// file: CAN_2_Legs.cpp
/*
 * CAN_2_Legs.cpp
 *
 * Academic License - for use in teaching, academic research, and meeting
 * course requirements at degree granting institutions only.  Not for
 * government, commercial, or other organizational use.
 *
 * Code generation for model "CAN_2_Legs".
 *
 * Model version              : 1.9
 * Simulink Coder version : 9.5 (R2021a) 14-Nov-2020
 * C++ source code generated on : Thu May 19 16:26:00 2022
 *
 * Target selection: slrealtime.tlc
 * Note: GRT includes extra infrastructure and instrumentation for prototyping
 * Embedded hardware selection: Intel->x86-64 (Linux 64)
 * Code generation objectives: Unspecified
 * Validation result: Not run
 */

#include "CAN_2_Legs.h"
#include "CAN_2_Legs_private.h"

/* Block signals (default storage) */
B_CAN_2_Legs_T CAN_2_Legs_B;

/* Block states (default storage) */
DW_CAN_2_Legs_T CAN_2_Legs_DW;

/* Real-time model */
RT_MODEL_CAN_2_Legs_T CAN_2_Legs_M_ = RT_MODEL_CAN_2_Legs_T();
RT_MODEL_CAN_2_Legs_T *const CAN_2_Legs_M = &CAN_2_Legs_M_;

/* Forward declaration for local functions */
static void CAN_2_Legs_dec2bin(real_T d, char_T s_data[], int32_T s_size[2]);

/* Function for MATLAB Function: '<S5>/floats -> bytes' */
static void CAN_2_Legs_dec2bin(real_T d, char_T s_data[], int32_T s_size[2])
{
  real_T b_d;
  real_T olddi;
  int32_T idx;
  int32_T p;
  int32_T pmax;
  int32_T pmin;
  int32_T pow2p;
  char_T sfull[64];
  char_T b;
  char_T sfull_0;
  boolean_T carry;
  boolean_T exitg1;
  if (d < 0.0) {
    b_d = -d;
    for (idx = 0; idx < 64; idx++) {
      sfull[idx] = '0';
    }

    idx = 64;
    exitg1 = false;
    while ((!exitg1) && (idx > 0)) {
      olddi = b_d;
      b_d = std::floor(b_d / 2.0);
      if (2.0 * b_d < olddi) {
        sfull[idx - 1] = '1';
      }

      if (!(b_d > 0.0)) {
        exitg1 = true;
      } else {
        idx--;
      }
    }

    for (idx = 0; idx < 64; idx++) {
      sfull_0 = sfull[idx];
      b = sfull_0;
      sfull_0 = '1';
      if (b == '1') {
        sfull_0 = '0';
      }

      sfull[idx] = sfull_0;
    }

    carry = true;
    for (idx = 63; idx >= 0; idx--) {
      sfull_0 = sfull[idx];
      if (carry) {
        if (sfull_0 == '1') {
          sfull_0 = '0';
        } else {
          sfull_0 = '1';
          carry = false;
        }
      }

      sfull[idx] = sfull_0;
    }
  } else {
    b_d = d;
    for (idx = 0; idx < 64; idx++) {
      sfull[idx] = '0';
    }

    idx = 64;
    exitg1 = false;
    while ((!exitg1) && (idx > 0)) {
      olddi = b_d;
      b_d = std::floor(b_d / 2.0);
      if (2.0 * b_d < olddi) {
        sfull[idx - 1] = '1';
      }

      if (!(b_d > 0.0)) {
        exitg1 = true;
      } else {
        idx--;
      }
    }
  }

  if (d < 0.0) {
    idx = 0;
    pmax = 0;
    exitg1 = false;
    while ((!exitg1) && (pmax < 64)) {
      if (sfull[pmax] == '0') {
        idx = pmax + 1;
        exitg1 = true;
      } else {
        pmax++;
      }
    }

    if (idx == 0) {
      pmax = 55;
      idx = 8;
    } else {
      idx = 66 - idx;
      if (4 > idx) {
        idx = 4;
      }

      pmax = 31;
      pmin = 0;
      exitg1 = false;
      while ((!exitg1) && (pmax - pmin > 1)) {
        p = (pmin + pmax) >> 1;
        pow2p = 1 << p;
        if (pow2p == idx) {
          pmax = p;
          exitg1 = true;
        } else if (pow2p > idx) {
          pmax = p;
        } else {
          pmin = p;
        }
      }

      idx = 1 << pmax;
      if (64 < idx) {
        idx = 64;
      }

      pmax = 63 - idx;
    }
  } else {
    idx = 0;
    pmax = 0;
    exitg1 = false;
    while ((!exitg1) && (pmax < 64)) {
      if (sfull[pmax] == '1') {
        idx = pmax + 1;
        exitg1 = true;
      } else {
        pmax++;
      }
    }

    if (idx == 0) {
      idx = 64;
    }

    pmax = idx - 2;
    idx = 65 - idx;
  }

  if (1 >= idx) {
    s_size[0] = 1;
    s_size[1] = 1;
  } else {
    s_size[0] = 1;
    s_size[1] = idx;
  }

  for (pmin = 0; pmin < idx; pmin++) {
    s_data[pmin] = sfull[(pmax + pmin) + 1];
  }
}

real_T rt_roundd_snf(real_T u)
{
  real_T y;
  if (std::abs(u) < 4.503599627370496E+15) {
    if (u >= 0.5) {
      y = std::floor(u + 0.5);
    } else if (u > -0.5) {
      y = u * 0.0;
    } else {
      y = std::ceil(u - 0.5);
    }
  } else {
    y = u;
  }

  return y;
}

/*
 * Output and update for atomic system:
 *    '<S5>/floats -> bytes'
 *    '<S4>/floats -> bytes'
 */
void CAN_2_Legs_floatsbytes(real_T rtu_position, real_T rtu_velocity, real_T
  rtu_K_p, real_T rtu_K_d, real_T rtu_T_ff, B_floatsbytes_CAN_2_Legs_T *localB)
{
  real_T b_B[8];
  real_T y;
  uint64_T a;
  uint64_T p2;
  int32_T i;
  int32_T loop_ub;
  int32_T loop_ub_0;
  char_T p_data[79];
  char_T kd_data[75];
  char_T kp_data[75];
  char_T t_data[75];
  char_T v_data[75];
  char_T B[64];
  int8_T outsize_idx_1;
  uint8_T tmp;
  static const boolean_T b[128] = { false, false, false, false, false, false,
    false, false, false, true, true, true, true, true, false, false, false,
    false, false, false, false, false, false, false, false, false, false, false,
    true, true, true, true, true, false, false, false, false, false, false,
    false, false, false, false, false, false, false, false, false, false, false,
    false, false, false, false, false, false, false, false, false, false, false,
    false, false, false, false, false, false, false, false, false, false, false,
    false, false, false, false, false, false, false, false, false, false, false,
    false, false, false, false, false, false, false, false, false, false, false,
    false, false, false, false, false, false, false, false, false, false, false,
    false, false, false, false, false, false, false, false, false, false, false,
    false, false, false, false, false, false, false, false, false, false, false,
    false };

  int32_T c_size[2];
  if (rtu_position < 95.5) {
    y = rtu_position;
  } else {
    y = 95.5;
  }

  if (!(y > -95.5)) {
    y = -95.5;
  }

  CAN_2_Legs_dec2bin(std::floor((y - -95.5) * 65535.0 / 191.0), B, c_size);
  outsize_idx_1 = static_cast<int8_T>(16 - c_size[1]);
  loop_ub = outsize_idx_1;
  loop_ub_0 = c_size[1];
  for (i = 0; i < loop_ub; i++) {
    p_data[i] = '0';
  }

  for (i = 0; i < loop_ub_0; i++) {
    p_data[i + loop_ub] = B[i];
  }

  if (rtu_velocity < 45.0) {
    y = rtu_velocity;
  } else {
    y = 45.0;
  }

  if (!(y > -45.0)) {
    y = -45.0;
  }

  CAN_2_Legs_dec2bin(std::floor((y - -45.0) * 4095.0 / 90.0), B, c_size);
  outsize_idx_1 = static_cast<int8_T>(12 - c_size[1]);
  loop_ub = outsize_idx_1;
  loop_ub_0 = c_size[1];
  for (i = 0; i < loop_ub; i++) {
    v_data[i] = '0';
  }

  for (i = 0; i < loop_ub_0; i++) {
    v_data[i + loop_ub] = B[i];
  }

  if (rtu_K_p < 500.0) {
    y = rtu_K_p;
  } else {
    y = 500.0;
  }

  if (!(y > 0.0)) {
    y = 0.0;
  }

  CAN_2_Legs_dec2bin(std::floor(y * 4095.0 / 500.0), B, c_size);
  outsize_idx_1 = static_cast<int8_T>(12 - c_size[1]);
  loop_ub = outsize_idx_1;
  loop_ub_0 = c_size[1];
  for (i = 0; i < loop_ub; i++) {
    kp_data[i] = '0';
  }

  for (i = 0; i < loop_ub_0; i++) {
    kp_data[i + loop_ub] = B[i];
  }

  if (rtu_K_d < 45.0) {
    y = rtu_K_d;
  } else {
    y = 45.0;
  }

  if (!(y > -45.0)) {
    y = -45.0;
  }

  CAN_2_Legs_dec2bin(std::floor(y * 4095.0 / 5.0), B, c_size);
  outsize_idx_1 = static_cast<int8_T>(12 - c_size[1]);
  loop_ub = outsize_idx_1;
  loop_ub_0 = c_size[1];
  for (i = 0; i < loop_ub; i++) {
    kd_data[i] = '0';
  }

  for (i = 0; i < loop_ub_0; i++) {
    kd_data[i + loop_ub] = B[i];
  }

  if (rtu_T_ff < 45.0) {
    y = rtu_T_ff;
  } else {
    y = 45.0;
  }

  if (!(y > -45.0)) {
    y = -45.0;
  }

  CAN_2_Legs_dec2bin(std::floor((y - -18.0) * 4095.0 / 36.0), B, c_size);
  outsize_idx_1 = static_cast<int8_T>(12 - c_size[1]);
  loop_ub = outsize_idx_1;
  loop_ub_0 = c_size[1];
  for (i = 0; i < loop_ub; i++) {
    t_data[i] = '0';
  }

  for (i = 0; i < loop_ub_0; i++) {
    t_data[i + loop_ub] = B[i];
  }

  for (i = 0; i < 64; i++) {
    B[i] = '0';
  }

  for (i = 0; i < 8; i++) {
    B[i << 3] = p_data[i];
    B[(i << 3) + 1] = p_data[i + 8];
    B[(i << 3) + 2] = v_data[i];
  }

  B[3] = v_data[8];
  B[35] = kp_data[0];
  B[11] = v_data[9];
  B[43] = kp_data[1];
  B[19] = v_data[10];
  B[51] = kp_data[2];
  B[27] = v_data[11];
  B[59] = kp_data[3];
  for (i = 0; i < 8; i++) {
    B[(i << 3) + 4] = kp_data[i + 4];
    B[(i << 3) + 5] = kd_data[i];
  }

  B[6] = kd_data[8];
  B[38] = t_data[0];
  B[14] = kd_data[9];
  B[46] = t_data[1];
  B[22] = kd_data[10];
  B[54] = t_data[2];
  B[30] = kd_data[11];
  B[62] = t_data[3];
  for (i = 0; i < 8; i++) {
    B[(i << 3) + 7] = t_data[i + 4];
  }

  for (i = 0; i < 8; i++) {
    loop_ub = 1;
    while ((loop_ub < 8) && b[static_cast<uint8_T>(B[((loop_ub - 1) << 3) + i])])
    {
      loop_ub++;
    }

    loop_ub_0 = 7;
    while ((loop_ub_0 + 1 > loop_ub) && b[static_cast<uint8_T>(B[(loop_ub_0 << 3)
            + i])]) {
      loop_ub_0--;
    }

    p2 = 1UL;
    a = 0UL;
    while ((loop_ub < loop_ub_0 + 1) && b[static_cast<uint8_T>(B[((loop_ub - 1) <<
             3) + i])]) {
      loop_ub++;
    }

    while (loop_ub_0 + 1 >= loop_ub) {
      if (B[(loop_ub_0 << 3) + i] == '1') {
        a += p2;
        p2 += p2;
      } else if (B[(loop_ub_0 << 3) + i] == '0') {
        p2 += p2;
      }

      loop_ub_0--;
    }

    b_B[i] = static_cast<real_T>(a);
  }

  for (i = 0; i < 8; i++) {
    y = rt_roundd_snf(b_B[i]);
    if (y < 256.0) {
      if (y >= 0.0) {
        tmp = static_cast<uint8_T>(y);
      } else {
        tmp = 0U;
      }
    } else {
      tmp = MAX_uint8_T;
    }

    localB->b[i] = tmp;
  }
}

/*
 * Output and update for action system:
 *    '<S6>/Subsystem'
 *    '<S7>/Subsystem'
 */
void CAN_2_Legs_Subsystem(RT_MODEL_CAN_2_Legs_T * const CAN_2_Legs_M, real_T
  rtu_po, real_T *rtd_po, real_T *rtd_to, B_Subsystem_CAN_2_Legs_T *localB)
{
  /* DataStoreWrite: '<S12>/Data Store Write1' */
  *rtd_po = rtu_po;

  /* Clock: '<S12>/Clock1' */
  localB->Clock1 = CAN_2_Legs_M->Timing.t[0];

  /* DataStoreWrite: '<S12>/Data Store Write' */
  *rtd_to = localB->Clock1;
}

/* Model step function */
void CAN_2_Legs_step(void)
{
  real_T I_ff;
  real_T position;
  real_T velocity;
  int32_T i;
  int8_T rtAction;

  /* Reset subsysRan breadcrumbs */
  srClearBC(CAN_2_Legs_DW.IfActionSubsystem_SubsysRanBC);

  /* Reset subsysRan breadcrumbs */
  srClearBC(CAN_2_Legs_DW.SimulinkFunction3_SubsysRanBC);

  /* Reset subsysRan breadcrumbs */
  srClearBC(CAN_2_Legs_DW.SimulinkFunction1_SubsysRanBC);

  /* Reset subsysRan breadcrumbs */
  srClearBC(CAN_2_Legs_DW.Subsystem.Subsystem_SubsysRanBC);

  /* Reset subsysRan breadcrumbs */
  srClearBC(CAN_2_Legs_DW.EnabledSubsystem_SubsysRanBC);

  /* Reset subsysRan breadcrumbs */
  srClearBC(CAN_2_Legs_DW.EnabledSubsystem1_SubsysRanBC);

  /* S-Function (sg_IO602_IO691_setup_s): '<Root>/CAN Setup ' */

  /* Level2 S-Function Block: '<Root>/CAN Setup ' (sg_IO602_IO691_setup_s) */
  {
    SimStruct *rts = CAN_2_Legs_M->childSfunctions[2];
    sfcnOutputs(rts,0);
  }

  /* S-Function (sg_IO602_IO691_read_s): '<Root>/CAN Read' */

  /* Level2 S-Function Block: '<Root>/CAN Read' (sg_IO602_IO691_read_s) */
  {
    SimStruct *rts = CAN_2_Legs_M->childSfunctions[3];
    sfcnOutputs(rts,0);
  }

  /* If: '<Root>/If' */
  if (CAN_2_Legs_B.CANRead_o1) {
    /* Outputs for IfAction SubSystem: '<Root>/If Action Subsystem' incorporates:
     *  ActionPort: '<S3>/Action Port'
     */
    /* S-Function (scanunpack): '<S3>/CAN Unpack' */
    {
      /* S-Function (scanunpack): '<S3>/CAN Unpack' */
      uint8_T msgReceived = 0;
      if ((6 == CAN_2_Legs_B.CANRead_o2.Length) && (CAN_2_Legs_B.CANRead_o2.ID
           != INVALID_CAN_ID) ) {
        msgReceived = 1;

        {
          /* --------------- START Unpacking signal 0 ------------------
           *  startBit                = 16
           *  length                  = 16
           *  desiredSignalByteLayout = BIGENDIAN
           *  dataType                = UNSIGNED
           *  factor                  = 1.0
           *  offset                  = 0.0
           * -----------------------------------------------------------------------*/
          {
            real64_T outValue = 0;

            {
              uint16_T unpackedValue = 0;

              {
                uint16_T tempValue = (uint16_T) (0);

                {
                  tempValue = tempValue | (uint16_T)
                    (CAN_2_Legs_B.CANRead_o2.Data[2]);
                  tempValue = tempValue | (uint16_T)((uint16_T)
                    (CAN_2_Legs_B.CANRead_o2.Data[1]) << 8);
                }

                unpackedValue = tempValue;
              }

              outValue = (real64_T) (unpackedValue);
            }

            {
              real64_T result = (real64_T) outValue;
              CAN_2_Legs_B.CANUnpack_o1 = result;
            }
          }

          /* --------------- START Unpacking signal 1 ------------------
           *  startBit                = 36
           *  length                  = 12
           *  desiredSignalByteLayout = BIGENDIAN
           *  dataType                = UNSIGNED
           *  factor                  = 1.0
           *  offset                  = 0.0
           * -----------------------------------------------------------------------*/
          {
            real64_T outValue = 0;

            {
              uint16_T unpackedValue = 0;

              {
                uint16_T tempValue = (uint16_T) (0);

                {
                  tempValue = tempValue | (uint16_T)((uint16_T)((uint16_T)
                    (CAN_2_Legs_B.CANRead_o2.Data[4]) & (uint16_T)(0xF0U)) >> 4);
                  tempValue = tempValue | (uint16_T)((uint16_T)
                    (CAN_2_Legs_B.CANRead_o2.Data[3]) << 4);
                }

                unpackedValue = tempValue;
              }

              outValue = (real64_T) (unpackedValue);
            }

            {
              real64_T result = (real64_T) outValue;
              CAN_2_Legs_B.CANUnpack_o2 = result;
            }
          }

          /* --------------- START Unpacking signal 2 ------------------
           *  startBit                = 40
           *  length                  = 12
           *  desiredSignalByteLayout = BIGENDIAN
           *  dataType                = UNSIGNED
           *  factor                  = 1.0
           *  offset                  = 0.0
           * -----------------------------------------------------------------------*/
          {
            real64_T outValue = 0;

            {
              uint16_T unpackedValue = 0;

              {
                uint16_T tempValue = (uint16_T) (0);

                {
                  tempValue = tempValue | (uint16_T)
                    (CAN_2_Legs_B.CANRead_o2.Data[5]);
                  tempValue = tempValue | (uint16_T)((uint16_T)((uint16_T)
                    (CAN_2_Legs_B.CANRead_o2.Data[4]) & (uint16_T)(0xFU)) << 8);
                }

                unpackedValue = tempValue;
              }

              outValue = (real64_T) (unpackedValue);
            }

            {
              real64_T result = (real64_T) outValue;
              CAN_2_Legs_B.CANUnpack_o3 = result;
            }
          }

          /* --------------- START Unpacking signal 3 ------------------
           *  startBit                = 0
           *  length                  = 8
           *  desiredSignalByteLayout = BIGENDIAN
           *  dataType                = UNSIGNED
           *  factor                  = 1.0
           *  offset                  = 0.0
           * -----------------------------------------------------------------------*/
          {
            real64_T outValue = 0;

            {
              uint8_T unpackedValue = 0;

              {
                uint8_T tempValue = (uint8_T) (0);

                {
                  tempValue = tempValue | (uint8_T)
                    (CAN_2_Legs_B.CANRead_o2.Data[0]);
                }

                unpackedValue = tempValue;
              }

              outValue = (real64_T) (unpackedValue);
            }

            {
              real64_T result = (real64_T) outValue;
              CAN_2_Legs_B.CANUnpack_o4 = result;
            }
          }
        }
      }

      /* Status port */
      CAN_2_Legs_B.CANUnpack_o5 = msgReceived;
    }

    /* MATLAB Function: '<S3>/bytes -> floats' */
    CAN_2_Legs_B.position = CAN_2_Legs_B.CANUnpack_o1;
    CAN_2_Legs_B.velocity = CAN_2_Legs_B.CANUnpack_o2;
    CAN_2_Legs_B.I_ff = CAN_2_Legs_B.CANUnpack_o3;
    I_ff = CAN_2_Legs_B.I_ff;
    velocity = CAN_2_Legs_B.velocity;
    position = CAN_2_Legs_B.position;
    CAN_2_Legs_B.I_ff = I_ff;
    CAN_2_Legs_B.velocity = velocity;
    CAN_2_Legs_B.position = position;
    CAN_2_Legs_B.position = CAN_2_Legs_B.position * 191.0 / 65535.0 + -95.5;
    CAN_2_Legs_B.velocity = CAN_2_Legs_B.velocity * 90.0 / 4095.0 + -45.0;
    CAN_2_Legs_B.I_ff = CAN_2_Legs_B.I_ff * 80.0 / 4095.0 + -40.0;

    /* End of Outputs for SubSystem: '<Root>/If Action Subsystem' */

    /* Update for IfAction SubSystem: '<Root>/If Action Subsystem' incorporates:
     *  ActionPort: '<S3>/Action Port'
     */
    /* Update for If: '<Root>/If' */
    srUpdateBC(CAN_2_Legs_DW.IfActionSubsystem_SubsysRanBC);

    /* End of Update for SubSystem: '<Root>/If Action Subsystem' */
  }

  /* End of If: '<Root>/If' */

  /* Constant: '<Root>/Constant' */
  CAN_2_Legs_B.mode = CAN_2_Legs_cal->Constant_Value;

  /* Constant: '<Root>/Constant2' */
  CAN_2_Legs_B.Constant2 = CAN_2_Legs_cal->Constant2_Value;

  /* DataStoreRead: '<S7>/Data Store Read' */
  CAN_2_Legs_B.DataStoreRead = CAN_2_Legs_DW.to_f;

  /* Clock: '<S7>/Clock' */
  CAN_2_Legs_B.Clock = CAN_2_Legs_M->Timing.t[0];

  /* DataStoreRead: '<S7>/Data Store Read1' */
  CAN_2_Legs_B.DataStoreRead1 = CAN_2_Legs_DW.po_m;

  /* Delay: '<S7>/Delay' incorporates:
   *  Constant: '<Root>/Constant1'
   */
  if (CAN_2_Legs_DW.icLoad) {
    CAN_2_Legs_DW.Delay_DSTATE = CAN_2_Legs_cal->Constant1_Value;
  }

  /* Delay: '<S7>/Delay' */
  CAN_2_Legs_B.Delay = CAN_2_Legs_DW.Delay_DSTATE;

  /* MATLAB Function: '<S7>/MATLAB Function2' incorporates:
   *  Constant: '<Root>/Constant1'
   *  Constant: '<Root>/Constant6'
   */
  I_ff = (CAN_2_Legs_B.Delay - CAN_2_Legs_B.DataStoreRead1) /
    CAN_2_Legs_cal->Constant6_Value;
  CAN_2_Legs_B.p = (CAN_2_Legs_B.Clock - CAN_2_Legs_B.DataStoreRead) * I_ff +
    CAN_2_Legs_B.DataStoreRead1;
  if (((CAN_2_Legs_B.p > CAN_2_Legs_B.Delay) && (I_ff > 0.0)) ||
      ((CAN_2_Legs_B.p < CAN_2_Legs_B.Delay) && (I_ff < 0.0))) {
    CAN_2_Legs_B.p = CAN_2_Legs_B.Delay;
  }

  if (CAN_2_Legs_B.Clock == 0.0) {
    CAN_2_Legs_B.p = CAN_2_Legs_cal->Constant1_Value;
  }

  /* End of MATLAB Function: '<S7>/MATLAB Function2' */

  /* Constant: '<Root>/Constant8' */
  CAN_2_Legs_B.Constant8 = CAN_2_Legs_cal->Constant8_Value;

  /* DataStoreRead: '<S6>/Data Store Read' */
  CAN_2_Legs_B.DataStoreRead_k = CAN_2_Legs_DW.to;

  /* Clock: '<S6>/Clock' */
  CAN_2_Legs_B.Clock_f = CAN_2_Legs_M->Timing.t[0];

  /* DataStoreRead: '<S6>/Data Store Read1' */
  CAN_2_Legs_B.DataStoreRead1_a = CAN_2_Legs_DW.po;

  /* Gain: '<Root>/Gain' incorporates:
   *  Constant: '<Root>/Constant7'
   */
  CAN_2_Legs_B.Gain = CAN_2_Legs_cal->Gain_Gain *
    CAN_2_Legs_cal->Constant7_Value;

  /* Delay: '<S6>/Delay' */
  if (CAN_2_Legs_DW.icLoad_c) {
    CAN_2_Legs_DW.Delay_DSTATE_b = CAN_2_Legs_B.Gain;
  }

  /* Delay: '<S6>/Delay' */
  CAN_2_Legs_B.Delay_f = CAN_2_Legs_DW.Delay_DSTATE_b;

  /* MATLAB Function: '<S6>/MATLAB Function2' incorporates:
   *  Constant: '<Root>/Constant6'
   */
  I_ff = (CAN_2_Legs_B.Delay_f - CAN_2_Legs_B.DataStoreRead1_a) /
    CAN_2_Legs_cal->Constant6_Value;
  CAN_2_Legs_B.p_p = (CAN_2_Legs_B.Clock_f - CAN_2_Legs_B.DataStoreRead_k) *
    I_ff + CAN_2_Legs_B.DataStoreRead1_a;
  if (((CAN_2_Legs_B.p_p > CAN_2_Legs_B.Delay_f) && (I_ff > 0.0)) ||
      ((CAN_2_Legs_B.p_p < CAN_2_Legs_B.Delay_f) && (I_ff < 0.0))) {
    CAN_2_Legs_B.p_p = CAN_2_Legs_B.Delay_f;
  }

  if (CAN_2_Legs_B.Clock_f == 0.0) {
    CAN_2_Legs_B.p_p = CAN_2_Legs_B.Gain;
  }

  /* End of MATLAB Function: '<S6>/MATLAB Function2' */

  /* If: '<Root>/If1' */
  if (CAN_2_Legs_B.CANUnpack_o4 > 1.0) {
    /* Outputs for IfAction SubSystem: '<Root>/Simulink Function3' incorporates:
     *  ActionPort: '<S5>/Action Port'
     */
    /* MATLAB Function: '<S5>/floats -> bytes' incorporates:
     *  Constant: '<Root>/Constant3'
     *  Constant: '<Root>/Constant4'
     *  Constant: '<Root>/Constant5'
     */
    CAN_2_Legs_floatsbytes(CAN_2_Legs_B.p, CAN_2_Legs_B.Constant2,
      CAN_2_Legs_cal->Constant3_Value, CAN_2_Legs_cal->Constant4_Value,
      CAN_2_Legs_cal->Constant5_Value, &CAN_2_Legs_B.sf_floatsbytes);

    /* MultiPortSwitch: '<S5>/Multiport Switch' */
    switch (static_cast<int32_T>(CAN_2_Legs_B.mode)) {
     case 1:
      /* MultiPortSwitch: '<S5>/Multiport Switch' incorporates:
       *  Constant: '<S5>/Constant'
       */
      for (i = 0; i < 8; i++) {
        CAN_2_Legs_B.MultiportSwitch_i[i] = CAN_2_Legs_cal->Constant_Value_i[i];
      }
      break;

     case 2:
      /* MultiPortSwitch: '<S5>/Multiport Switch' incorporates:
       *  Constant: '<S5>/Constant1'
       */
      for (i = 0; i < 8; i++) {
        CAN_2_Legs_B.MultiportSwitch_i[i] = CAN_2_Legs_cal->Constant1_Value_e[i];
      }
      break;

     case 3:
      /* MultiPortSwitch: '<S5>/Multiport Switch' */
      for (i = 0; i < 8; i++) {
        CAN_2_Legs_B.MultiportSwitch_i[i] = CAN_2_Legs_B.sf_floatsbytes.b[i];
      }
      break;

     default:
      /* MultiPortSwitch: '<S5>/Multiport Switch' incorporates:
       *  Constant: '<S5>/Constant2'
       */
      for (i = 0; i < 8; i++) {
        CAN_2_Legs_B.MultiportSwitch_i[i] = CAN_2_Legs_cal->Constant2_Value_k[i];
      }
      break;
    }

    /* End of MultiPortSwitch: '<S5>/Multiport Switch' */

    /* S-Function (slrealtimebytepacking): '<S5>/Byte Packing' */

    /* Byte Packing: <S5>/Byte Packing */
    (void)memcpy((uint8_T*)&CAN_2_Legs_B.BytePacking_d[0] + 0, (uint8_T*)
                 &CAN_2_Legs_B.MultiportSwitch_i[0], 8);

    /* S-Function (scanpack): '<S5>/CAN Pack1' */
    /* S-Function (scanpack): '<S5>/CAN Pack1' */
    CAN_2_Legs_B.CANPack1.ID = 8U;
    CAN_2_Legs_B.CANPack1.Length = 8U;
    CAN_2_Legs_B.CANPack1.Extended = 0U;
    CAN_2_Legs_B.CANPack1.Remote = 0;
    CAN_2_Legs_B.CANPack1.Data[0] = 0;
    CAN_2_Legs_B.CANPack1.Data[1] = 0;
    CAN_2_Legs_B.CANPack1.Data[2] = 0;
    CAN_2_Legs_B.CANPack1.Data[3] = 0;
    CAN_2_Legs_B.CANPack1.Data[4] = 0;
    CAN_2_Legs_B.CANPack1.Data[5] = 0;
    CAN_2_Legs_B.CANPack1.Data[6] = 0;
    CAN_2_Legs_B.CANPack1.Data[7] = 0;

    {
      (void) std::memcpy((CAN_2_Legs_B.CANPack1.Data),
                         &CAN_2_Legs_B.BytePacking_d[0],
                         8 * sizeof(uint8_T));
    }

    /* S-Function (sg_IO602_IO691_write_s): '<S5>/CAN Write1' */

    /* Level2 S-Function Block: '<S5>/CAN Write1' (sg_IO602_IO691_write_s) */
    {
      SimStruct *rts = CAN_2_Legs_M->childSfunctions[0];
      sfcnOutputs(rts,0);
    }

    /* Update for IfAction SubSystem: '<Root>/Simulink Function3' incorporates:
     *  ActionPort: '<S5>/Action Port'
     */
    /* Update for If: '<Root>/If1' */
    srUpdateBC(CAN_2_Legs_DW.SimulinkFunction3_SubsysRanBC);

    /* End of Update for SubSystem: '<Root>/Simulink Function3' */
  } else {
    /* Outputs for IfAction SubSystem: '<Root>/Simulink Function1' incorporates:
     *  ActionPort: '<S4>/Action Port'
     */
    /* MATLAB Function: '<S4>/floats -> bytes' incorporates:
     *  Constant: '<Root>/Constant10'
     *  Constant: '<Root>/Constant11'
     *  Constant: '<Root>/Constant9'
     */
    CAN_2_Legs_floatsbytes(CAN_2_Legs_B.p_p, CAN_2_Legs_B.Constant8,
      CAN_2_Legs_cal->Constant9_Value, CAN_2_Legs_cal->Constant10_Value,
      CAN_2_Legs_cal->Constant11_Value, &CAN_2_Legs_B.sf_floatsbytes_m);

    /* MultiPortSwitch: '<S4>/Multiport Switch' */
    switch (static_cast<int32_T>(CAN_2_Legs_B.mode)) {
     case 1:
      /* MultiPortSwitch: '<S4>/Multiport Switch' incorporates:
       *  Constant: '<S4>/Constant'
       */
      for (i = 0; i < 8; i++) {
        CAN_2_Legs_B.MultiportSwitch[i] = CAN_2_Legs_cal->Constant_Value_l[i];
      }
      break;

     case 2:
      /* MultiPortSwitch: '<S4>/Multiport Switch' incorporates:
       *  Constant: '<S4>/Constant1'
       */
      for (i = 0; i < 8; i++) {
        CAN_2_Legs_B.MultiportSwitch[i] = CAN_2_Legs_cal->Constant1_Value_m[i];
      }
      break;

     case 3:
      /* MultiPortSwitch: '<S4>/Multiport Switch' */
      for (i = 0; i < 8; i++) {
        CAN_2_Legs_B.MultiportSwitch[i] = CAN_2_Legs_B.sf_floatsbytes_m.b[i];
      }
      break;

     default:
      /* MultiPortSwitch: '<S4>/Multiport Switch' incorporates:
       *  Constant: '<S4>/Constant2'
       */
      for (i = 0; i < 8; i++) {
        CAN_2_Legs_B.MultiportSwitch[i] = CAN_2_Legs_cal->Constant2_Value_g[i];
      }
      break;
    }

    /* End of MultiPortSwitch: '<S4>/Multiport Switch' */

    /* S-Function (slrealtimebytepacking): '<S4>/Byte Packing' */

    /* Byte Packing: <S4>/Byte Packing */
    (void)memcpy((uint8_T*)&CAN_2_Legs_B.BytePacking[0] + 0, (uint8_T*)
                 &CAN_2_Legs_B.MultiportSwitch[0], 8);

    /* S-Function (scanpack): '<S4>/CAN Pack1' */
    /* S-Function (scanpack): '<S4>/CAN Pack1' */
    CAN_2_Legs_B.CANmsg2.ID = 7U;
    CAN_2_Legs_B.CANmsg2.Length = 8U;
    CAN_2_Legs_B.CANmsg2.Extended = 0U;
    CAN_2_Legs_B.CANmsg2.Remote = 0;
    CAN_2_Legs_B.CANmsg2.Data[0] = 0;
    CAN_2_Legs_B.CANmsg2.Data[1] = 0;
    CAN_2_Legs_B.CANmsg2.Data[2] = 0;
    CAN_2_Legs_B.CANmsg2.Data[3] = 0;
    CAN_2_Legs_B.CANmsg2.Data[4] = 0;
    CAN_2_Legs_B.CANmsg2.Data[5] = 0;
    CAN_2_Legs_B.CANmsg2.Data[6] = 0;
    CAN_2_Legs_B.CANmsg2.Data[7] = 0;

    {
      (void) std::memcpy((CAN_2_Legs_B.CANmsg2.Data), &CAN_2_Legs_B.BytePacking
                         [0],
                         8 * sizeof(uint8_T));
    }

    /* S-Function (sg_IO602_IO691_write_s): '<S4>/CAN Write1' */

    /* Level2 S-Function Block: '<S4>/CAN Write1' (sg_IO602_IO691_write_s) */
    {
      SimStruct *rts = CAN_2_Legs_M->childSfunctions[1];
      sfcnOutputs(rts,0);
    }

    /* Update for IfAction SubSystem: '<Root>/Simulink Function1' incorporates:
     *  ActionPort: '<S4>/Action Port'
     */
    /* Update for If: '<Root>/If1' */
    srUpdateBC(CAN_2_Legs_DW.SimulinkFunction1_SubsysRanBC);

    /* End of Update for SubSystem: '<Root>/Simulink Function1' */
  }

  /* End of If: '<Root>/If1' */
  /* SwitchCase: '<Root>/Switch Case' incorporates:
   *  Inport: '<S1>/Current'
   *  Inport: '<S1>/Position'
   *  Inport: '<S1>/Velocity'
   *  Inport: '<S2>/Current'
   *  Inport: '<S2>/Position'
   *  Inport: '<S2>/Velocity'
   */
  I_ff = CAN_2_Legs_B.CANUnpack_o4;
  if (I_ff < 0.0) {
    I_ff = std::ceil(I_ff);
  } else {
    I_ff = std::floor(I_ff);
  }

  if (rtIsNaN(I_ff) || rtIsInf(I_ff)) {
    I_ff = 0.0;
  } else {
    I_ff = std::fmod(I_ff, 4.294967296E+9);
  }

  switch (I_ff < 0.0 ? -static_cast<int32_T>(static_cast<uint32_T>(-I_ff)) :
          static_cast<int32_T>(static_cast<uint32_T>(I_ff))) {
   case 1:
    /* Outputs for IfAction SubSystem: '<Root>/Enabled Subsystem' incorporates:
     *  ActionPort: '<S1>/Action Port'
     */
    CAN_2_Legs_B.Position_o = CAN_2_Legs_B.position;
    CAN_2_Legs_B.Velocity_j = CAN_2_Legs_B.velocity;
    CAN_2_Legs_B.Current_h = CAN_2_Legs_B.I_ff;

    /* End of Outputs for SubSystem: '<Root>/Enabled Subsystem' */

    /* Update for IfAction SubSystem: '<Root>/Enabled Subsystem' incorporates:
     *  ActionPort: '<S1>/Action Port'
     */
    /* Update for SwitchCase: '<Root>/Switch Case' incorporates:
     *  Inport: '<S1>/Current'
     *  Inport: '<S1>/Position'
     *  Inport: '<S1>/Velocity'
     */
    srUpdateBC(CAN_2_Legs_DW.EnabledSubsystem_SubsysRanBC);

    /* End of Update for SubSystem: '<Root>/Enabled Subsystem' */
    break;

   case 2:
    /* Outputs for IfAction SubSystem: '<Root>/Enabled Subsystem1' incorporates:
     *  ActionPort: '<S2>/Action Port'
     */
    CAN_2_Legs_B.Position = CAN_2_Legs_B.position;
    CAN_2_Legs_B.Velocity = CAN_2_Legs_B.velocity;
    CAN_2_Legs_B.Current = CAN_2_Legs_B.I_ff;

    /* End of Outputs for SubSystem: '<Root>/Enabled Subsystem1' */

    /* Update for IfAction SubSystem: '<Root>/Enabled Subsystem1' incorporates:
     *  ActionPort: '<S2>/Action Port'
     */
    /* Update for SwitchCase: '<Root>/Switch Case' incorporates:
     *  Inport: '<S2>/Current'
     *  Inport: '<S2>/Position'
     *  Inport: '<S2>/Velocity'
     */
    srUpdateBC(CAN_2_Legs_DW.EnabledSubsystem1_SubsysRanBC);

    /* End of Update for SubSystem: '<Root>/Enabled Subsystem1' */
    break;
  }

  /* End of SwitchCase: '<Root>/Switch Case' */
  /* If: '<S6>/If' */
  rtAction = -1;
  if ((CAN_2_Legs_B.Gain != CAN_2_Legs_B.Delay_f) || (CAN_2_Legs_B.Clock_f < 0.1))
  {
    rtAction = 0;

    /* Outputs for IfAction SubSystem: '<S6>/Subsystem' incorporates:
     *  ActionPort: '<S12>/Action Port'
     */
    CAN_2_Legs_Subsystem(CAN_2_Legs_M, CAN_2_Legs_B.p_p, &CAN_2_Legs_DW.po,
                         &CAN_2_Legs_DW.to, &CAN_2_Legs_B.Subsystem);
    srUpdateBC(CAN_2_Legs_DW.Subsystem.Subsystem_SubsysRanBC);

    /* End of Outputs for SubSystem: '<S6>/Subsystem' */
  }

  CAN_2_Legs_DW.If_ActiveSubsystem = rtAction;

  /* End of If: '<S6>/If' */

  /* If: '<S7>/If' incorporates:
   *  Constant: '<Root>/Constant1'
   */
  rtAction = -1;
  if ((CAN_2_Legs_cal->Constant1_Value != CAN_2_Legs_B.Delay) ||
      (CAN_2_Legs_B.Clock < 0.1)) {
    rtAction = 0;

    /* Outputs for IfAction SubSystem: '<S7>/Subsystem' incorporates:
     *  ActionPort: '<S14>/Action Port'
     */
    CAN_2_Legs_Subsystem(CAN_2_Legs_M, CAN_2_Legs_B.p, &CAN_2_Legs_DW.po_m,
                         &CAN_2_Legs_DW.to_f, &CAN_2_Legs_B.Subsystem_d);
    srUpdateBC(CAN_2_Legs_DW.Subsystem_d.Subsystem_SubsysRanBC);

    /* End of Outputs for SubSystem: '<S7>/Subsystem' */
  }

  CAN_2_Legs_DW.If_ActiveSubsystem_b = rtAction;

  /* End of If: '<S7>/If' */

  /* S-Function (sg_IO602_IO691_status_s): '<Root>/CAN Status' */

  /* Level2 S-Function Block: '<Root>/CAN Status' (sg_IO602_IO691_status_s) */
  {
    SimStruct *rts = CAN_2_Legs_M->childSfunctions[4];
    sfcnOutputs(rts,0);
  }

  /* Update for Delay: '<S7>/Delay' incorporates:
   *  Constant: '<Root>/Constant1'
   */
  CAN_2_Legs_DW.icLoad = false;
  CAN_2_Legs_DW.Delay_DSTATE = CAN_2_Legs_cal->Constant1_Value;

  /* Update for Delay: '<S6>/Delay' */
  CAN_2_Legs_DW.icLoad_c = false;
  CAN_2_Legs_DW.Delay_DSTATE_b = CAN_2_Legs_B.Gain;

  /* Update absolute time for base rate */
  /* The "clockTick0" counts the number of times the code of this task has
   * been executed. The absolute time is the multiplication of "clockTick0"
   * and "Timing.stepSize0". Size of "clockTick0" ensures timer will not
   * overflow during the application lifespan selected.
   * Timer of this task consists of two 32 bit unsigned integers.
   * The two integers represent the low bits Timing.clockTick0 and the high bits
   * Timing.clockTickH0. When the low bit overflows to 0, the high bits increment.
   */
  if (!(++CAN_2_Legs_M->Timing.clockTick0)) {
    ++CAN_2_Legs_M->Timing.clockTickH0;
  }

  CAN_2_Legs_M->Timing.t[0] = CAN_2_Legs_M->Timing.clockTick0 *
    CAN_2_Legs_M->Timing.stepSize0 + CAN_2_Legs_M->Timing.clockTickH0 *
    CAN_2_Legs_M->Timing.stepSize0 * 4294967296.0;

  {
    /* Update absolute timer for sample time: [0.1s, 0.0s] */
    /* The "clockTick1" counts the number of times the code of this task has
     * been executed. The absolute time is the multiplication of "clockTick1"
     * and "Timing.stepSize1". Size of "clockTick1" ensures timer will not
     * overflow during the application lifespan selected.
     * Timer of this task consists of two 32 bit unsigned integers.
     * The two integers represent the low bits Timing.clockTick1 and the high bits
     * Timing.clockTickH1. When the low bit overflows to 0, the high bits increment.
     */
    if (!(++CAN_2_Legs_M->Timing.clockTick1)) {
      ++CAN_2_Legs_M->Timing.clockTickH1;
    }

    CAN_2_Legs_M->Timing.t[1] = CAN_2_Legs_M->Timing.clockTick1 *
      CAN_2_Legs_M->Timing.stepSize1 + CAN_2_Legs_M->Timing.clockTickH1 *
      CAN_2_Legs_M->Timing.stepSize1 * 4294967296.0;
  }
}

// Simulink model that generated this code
simulink model "CAN_2_Legs"  (R2021a)
settings: Solver=FixedStepAuto  StartTime=0.0  StopTime=200  FixedStep=.1  RelTol=1e-3
libraries: speedgoatlib_IO691 x5, canmsglib x3, slrealtimeutilitieslib x2

== system CAN_2_Legs ==
  Add : Sum  Commented=on  Inputs=-+
  CAN Read : speedgoatlib_IO691/CAN Read  id=1  ts=-1  channel=1  messageType=CAN  canType=CAN (HS)  initValues=[691 1 -1 0 1 1]
  "CAN Setup " : speedgoatlib_IO691/CAN Setup   moduletype=IO691  id=1  pciSlot=-1  chn1=CAN (HS)  chn2=CAN (HS)  chn3=Disabled  chn4=Disabled  initStruct=[]  termStruct=[]  ArbitrationbdrChn1=1.0 MBaud  ArbitrationManbdrChn1=[2,8,31,8]  FdbdrChn1=5.0 MBaud  FdManbdrChn1=[2,2,5,2]  ArbitrationbdrChn2=1.0 MBaud  ArbitrationManbdrChn2=[2,8,31,8]  FdbdrChn2=5.0 MBaud  FdManbdrChn2=[2,2,5,2]  ArbitrationbdrChn3=1.0 MBaud  ArbitrationManbdrChn3=[2,8,31,8]  FdbdrChn3=5.0 MBaud  FdManbdrChn3=[2,2,5,2]  ArbitrationbdrChn4=1.0 MBaud  ArbitrationManbdrChn4=[2,8,31,8]  FdbdrChn4=5.0 MBaud  FdManbdrChn4=[2,2,5,2]  moduleInitValues=[691 1 -1 -1]
  CAN Status : speedgoatlib_IO691/CAN Status  moduleId=1  sampleTime=-1  channel=1  busRecovery=Off  arrayOutput=off  controllerCpuLoad=off  controllerLiveCount=off  initModeAct=off  avgBusLoad=off  receiving=off  RxQueueEmpty=off  dataOverrunRcv=off  rxBufferLevel=off  txPending=off  dataOverrunTx=off  txBufferLevel=off  errWarnLimit=off  errPassLimit=off  errBusOff=off  busRecoveryCounter=off  busCouplingErr=off  transceiverErr=off  opMode=off  brp=off  timeSegment1=off  timeSegment2=off  synchronisationJumpWidth=off  dataTSEG1=off  dataTSEG2=off  dataSJW=off  moduleType=691  qtyStatBlk=1  ptIdx=0  isFDMod=0
  Constant : Constant  Value=3
  Constant1 : Constant  Value=0.5
  Constant10 : Constant  Value=0.1
  Constant{2,5,8,11} (4 alike) : Constant  Value=0
  Constant3 : Constant  Value=6
  Constant4 : Constant  Value=0.1
  Constant6 : Constant  Value=3
  Constant7 : Constant  Value=-0.5
  Constant9 : Constant  Value=10
  Enabled Subsystem : Subsystem  TreatAsAtomicUnit=on
  Enabled Subsystem1 : Subsystem  TreatAsAtomicUnit=on
  Gain : Gain  Gain=18/30
  If : If  IfExpression=u1 ~= 0  ShowElse=off
  If Action Subsystem : Subsystem  TreatAsAtomicUnit=on
  If1 : If  IfExpression=u1 > 1
  Kd : EditField  LabelPosition=Hide  ShowInitialText=on  Alignment=Center
  Kd1 : EditField  LabelPosition=Hide  ShowInitialText=on  Alignment=Center
  Kp : EditField  LabelPosition=Hide  ShowInitialText=on  Alignment=Center
  Kp1 : EditField  LabelPosition=Hide  ShowInitialText=on  Alignment=Center
  MATLAB Function : MATLAB Function  Commented=on  TreatAsAtomicUnit=on
  MATLAB Function1 : MATLAB Function  Commented=on  TreatAsAtomicUnit=on
  Mux : Mux  Inputs=5
  Mux1 : Mux  Inputs=5
  Mux2 : Mux  Commented=on  Inputs=2
  Position : EditField  LabelPosition=Hide  ShowInitialText=on  Alignment=Center
  Position2 : EditField  LabelPosition=Hide  ShowInitialText=on  Alignment=Center
  Rotary Switch : RotarySwitchBlock
  Simulink Function1 : Subsystem  TreatAsAtomicUnit=on
  Simulink Function3 : Subsystem  TreatAsAtomicUnit=on
  Subsystem : Subsystem
  Subsystem2 : Subsystem
  Switch Case : SwitchCase  CaseConditions={1,2}  ShowDefaultCase=off
  Tff : EditField  LabelPosition=Hide  ShowInitialText=on  Alignment=Center
  Tff1 : EditField  LabelPosition=Hide  ShowInitialText=on  Alignment=Center
  Time : EditField  LabelPosition=Hide  ShowInitialText=on  Alignment=Center
  Velocity : EditField  LabelPosition=Hide  ShowInitialText=on  Alignment=Center
  Velocity1 : EditField  LabelPosition=Hide  ShowInitialText=on  Alignment=Center
  wires:
  Mux/1 -> Simulink Function3/2(Command)
  Constant2/1 -> Mux/2
  Constant1/1 -> Add/1, Subsystem2/1(pf), Subsystem2/2(pc)
  Constant3/1 -> Mux/3
  Constant4/1 -> Mux/4
  Constant5/1 -> Mux/5
  Constant10/1 -> Mux1/4
  Constant8/1 -> Mux1/2
  Mux1/1 -> Simulink Function1/2(Command)
  Constant9/1 -> Mux1/3
  Constant/1 -> Simulink Function3/1(Mode), Simulink Function1/1(Mode)  "mode"
  Constant11/1 -> Mux1/5
  Mux2/1 -> MATLAB Function1/1(Pmux)
  ? -> Add/2, MATLAB Function/3(P1)  "P_1"
  ? -> MATLAB Function/1(Iff)  "I_1"
  MATLAB Function/1(GRF) -> ?  "GRF"
  Add/1 -> ?  "pc-p1"
  ? -> ?  "V_1"
  MATLAB Function1/1(danger) -> ?  "danger"
  Subsystem2/1(p) -> Mux/1
  Subsystem/1(p) -> Mux1/1
  Constant6/1 -> Subsystem/2(tstep), Subsystem2/3(tstep)
  Gain/1 -> Subsystem/1(pc), Subsystem/3(pf)
  If Action Subsystem/5(Status) -> ?
  If Action Subsystem/2(Velocity) -> Enabled Subsystem1/2(Velocity), Enabled Subsystem/2(Velocity)  "V_out"
  If Action Subsystem/3(Current) -> Enabled Subsystem1/3(Current), Enabled Subsystem/3(Current)
  CAN Read/2 -> If Action Subsystem/1(In1)
  If Action Subsystem/1(Position) -> Enabled Subsystem1/1(Position), Enabled Subsystem/1(Position)  "P_out"
  CAN Read/1 -> If/1
  If/1 -> If Action Subsystem/Action
  If Action Subsystem/4(ID) -> If1/1, Switch Case/1  "ID"
  Switch Case/2 -> Enabled Subsystem1/Action
  Enabled Subsystem/1(P1) -> ?  "P1"
  Enabled Subsystem1/1(P2) -> ?  "P2"
  Enabled Subsystem1/3(I2) -> ?  "I2"
  Enabled Subsystem/3(I1) -> ?  "I1"
  Constant7/1 -> Gain/1
  Enabled Subsystem/2(V1) -> ?  "V1"
  Enabled Subsystem1/2(V2) -> ?  "V1"
  Switch Case/1 -> Enabled Subsystem/Action
  If1/2 -> Simulink Function1/Action
  If1/1 -> Simulink Function3/Action

== system CAN_2_Legs/Enabled Subsystem ==
  Position : Inport
  Velocity : Inport  Port=2
  Current : Inport  Port=3
  Action Port : ActionPort  ActionPortLabel=case [ 1 ]:
  P1 : Outport
  V1 : Outport  Port=2
  I1 : Outport  Port=3
  wires:
  Position/1 -> P1/1
  Velocity/1 -> V1/1
  Current/1 -> I1/1

== system CAN_2_Legs/Enabled Subsystem1 ==
  Position : Inport
  Velocity : Inport  Port=2
  Current : Inport  Port=3
  Action Port : ActionPort  ActionPortLabel=case [ 2 ]:
  P2 : Outport
  V2 : Outport  Port=2
  I2 : Outport  Port=3
  wires:
  Position/1 -> P2/1
  Velocity/1 -> V2/1
  Current/1 -> I2/1

== system CAN_2_Legs/If Action Subsystem ==
  In1 : Inport
  Action Port : ActionPort  ActionPortLabel=if(u1 ~= 0)
  CAN Unpack : canmsglib/CAN Unpack  MsgList=(none)  MsgName=CAN Msg  MsgIDType=Standard (11-bit identifier)  MsgIdentifier=-1  MsgLength=6  SignalInfo={ 'position', '16', '16', 'BE', 'unsigned', 'Standard', '0', '1', '0', '0', '65535'; 'velocity', '36', '12', 'BE', 'unsigned', 'Standard', '0', '1', '0', '0', '4095'; 'current', '40', '12', 'BE', 'unsigned', 'Standard', '0', '1', '0', '0', '4095'; 'id', '0', '8', 'BE', 'unsigned', 'Standard', '0', '1', '0', '0', '255' }  IDPort=off  TimestampPort=off  ErrorPort=off  RemotePort=off  LengthPort=off  StatusPort=on  ApplyMinMax=off
  "bytes -> floats" : MATLAB Function  TreatAsAtomicUnit=on
  Position : Outport
  Velocity : Outport  Port=2
  Current : Outport  Port=3
  ID : Outport  Port=4
  Status : Outport  Port=5
  wires:
  CAN Unpack/5 -> Status/1
  CAN Unpack/1 -> "bytes -> floats"/1("position ")
  CAN Unpack/3 -> "bytes -> floats"/3("I_ff ")
  "bytes -> floats"/1(position) -> Position/1
  CAN Unpack/4 -> ID/1
  "bytes -> floats"/2(velocity) -> Velocity/1
  "bytes -> floats"/3(I_ff) -> Current/1  "I_ff"
  CAN Unpack/2 -> "bytes -> floats"/2("velocity ")
  In1/1 -> CAN Unpack/1

== system CAN_2_Legs/Simulink Function1 ==
  Mode : Inport
  Command : Inport  Port=2
  Action Port : ActionPort  ActionPortLabel=else
  Byte Packing : slrealtimeutilitieslib/Byte Packing  MaskPackedDataType=uint8  MaskUnpackedDataTypes={['uint8']}  MaskAlignment=1
  CAN Pack1 : canmsglib/CAN Pack  MsgList=(none)  MsgName=CAN Msg  MsgIDType=Standard (11-bit identifier)  MsgIdentifier=2  MsgLength=8  Remote=off  ApplyMinMax=off  BusOutput=off  SignalInfo={ 'b1', '0', '8', 'LE', 'unsigned', 'Standard', '0', '1', '0', '-Inf', 'Inf'; 'b2', '8', '8', 'LE', 'unsigned', 'Standard', '0', '1', '0', '-Inf', 'Inf'; 'b3', '16', '8', 'LE', 'unsigned', 'Standard', '0', '1', '0', '-Inf', 'Inf'; 'b4', '24', '8', 'LE', 'unsigned', 'Standard', '0', '1', '0', '-Inf', 'Inf'; 'b5', '32', '8', 'LE', 'unsigned', 'Standard', '0', '1', '0', '-Inf', 'Inf'; 'b6', '40', '8', 'LE', 'unsigned', 'Standard', '0', '1', '0', '-Inf', 'Inf'; 'b7', '48', '8', 'LE', 'unsigned', 'Standard', '0', '1', '0', '-Inf', 'Inf'; 'b8', '56', '8', 'LE', 'unsigned', 'Standard', '0', '1', '0', '-Inf', 'Inf' }
  CAN Write1 : speedgoatlib_IO691/CAN Write  id=1  ts=-1  channel=1  messageType=CAN  enableStatusPort=off  canType=CAN (HS)  initValues=[691 1 -1 0 1 1 0]
  Constant : Constant  Value=[0xFF, 0xFF, 0xFF, 0xFF, 0xFF, 0xFF, 0xFF, 0xFE]
  Constant1 : Constant  Value=[0xFF, 0xFF, 0xFF, 0xFF, 0xFF, 0xFF, 0xFF, 0xFC]
  Constant2 : Constant  Value=[0xFF, 0xFF, 0xFF, 0xFF, 0xFF, 0xFF, 0xFF, 0xFD]
  Demux : Demux  Outputs=5
  Multiport Switch : MultiPortSwitch  Inputs=4
  "floats -> bytes" : MATLAB Function  TreatAsAtomicUnit=on
  wires:
  Demux/5 -> "floats -> bytes"/5(T_ff)
  Multiport Switch/1 -> Byte Packing/1
  Demux/4 -> "floats -> bytes"/4(K_d)
  Demux/1 -> "floats -> bytes"/1(position)  "P_in"
  Constant/1 -> Multiport Switch/2  "Zero"
  Demux/2 -> "floats -> bytes"/2(velocity)  "V_in"
  Constant2/1 -> Multiport Switch/5  "Deinitiate"
  CAN Pack1/1 -> CAN Write1/1  "CAN msg 2"
  Byte Packing/1 -> CAN Pack1/1
  Constant1/1 -> Multiport Switch/3  "Initiate"
  "floats -> bytes"/1(b) -> Multiport Switch/4
  Demux/3 -> "floats -> bytes"/3(K_p)
  Mode/1 -> Multiport Switch/1
  Command/1 -> Demux/1

== system CAN_2_Legs/Simulink Function3 ==
  Mode : Inport
  Command : Inport  Port=2
  Action Port : ActionPort  ActionPortLabel=if(u1 > 1)
  Byte Packing : slrealtimeutilitieslib/Byte Packing  MaskPackedDataType=uint8  MaskUnpackedDataTypes={['uint8']}  MaskAlignment=1
  CAN Pack1 : canmsglib/CAN Pack  MsgList=(none)  MsgName=CAN Msg  MsgIDType=Standard (11-bit identifier)  MsgIdentifier=1  MsgLength=8  Remote=off  ApplyMinMax=off  BusOutput=off  SignalInfo={ 'b1', '0', '8', 'LE', 'unsigned', 'Standard', '0', '1', '0', '-Inf', 'Inf'; 'b2', '8', '8', 'LE', 'unsigned', 'Standard', '0', '1', '0', '-Inf', 'Inf'; 'b3', '16', '8', 'LE', 'unsigned', 'Standard', '0', '1', '0', '-Inf', 'Inf'; 'b4', '24', '8', 'LE', 'unsigned', 'Standard', '0', '1', '0', '-Inf', 'Inf'; 'b5', '32', '8', 'LE', 'unsigned', 'Standard', '0', '1', '0', '-Inf', 'Inf'; 'b6', '40', '8', 'LE', 'unsigned', 'Standard', '0', '1', '0', '-Inf', 'Inf'; 'b7', '48', '8', 'LE', 'unsigned', 'Standard', '0', '1', '0', '-Inf', 'Inf'; 'b8', '56', '8', 'LE', 'unsigned', 'Standard', '0', '1', '0', '-Inf', 'Inf' }
  CAN Write1 : speedgoatlib_IO691/CAN Write  id=1  ts=-1  channel=1  messageType=CAN  enableStatusPort=off  canType=CAN (HS)  initValues=[691 1 -1 0 1 1 0]
  Constant : Constant  Value=[0xFF, 0xFF, 0xFF, 0xFF, 0xFF, 0xFF, 0xFF, 0xFE]
  Constant1 : Constant  Value=[0xFF, 0xFF, 0xFF, 0xFF, 0xFF, 0xFF, 0xFF, 0xFC]
  Constant2 : Constant  Value=[0xFF, 0xFF, 0xFF, 0xFF, 0xFF, 0xFF, 0xFF, 0xFD]
  Demux : Demux  Outputs=5
  Multiport Switch : MultiPortSwitch  Inputs=4
  "floats -> bytes" : MATLAB Function  TreatAsAtomicUnit=on
  wires:
  Demux/5 -> "floats -> bytes"/5(T_ff)
  Multiport Switch/1 -> Byte Packing/1
  Demux/4 -> "floats -> bytes"/4(K_d)
  Demux/1 -> "floats -> bytes"/1(position)  "P_in"
  Constant/1 -> Multiport Switch/2  "Zero"
  Demux/2 -> "floats -> bytes"/2(velocity)  "V_in"
  Constant2/1 -> Multiport Switch/5  "Deinitiate"
  CAN Pack1/1 -> CAN Write1/1
  Byte Packing/1 -> CAN Pack1/1
  Constant1/1 -> Multiport Switch/3  "Initiate"
  "floats -> bytes"/1(b) -> Multiport Switch/4
  Demux/3 -> "floats -> bytes"/3(K_p)
  Mode/1 -> Multiport Switch/1
  Command/1 -> Demux/1

== system CAN_2_Legs/Subsystem ==
  pc : Inport
  tstep : Inport  Port=2
  pf : Inport  Port=3
  Clock : Clock
  Data Store Memory : DataStoreMemory  DataStoreName=to  ReadBeforeWriteMsg=warning  WriteAfterWriteMsg=warning  WriteAfterReadMsg=warning  ShowAdditionalParam=off
  Data Store Memory1 : DataStoreMemory  DataStoreName=po  ReadBeforeWriteMsg=warning  WriteAfterWriteMsg=warning  WriteAfterReadMsg=warning  ShowAdditionalParam=off
  Data Store Read : DataStoreRead  DataStoreName=to  IndexOptions=Index vector (dialog)  Indices=1  OutputSizes=1
  Data Store Read1 : DataStoreRead  DataStoreName=po  IndexOptions=Index vector (dialog)  Indices=1  OutputSizes=1
  Delay : Delay  DelayLength=1  InitialConditionSource=Input port
  If : If  NumInputs=3  IfExpression=u1 ~= u2 | u3<.1  ShowElse=off
  MATLAB Function2 : MATLAB Function  TreatAsAtomicUnit=on
  Subsystem : Subsystem
  p : Outport
  wires:
  Clock/1 -> MATLAB Function2/2(t), If/3
  MATLAB Function2/1(p) -> Subsystem/1(po), p/1
  tstep/1 -> MATLAB Function2/6(tstep)
  pf/1 -> Delay/2, Delay/1, If/1
  If/1 -> Subsystem/Action
  Delay/1 -> MATLAB Function2/4(pf), If/2
  Data Store Read/1 -> MATLAB Function2/1(to)
  Data Store Read1/1 -> MATLAB Function2/3(po)
  pc/1 -> MATLAB Function2/5(pc)

== system CAN_2_Legs/Subsystem2 ==
  pf : Inport
  pc : Inport  Port=2
  tstep : Inport  Port=3
  Clock : Clock
  Data Store Memory : DataStoreMemory  DataStoreName=to  ReadBeforeWriteMsg=warning  WriteAfterWriteMsg=warning  WriteAfterReadMsg=warning  ShowAdditionalParam=off
  Data Store Memory1 : DataStoreMemory  DataStoreName=po  ReadBeforeWriteMsg=warning  WriteAfterWriteMsg=warning  WriteAfterReadMsg=warning  ShowAdditionalParam=off
  Data Store Read : DataStoreRead  DataStoreName=to  IndexOptions=Index vector (dialog)  Indices=1  OutputSizes=1
  Data Store Read1 : DataStoreRead  DataStoreName=po  IndexOptions=Index vector (dialog)  Indices=1  OutputSizes=1
  Delay : Delay  DelayLength=1  InitialConditionSource=Input port
  If : If  NumInputs=3  IfExpression=u1 ~= u2 | u3<.1  ShowElse=off
  MATLAB Function2 : MATLAB Function  TreatAsAtomicUnit=on
  Subsystem : Subsystem
  p : Outport
  wires:
  Clock/1 -> MATLAB Function2/2(t), If/3
  MATLAB Function2/1(p) -> Subsystem/1(po), p/1
  tstep/1 -> MATLAB Function2/6(tstep)
  pf/1 -> Delay/2, Delay/1, If/1
  If/1 -> Subsystem/Action
  Delay/1 -> MATLAB Function2/4(pf), If/2
  Data Store Read/1 -> MATLAB Function2/1(to)
  Data Store Read1/1 -> MATLAB Function2/3(po)
  pc/1 -> MATLAB Function2/5(pc)

== system CAN_2_Legs/Subsystem/Subsystem ==
  po : Inport
  Action Port : ActionPort  ActionPortLabel=if(u1 ~= u2 | u3<.1)
  Clock1 : Clock
  Data Store Write : DataStoreWrite  DataStoreName=to  IndexOptions=Index vector (dialog)  Indices=1  OutputSizes=1
  Data Store Write1 : DataStoreWrite  DataStoreName=po  IndexOptions=Index vector (dialog)  Indices=1  OutputSizes=1
  wires:
  Clock1/1 -> Data Store Write/1
  po/1 -> Data Store Write1/1

== system CAN_2_Legs/Subsystem2/Subsystem ==
  po : Inport
  Action Port : ActionPort  ActionPortLabel=if(u1 ~= u2 | u3<.1)
  Clock1 : Clock
  Data Store Write : DataStoreWrite  DataStoreName=to  IndexOptions=Index vector (dialog)  Indices=1  OutputSizes=1
  Data Store Write1 : DataStoreWrite  DataStoreName=po  IndexOptions=Index vector (dialog)  Indices=1  OutputSizes=1
  wires:
  Clock1/1 -> Data Store Write/1
  po/1 -> Data Store Write1/1

== matlab function CAN_2_Legs/If Action Subsystem/bytes -> floats ==
function [position, velocity, I_ff] = fcn(position, velocity, I_ff)

P_MIN  =-95.5;  % [rad]
P_MAX  = 95.5;  % [rad]
V_MIN  =-45;    % [rad/s]
V_MAX  = 45;    % [rad/s]
I_MIN  =-40;    % []
I_MAX  = 40;    % []

position = position*(P_MAX  - P_MIN)/65535+ P_MIN;
velocity = velocity*(V_MAX  - V_MIN)/4095 + V_MIN;
I_ff     = I_ff*(I_MAX  - I_MIN)/4095 + I_MIN;

== matlab function CAN_2_Legs/Simulink Function1/floats -> bytes ==
function b = fcn(position, velocity, K_p, K_d, T_ff)

P_MIN  =-95.5;  % [rad]
P_MAX  = 95.5;  % [rad]
V_MIN  =-45;    % [rad/s] 30 to 45
V_MAX  = 45;    % [rad/s]
KP_MIN = 0;     % [Nm/rad]
KP_MAX = 500;   % [Nm/rad]
KD_MIN = 0;     % [Nm*s/rad
KD_MAX = 5;     % [Nm*s/rad
T_MIN  =-18;    % [Nm]
T_MAX  = 18;    % [Nm]

position = floor((max(min(position,P_MAX) ,P_MIN)  - P_MIN )*65535/(P_MAX  - P_MIN));
velocity = floor((max(min(velocity,V_MAX) ,V_MIN)  - V_MIN )*4095 /(V_MAX  - V_MIN));
K_p      = floor((max(min(K_p     ,KP_MAX),KP_MIN) - KP_MIN)*4095 /(KP_MAX - KP_MIN));
K_d      = floor((max(min(K_d     ,V_MAX) ,V_MIN)  - KD_MIN)*4095 /(KD_MAX - KD_MIN));
T_ff     = floor((max(min(T_ff    ,V_MAX) ,V_MIN)  - T_MIN )*4095 /(T_MAX  - T_MIN));

p  = dec2bin(position);
p  = [repmat('0', 1, 16-length(p)),p];
v  = dec2bin(velocity);
v  = [repmat('0', 1, 12-length(v)),v];
kp = dec2bin(K_p);
kp  = [repmat('0', 1, 12-length(kp)),kp];
kd = dec2bin(K_d);
kd  = [repmat('0', 1, 12-length(kd)),kd];
t  = dec2bin(T_ff);
t  = [repmat('0', 1, 12-length(t)),t];

B = repmat('0', 8, 8);

B(1,:) = p(1:8);
B(2,:) = p(9:16);
B(3,:) = v(1:8);
B(4,:) = [v(9:12),kp(1:4)];
B(5,:) = kp(5:12);
B(6,:) = kd(1:8);
B(7,:) = [kd(9:12),t(1:4)];
B(8,:) = t(5:12);

B  = bin2dec(B);

b = uint8(B);

== matlab function CAN_2_Legs/MATLAB Function ==
function GRF = isGRF(Iff, Pc,P1)
    GRF = 0;
    threshhold = 2.25;
    delP = Pc - P1;
    
    if((P1<0 && threshhold<Iff)|| (P1>0 && -threshhold>Iff))
        GRF = 1;
    end

== matlab function CAN_2_Legs/Simulink Function3/floats -> bytes ==
function b = fcn(position, velocity, K_p, K_d, T_ff)

P_MIN  =-95.5;  % [rad]
P_MAX  = 95.5;  % [rad]
V_MIN  =-45;    % [rad/s] 30 to 45
V_MAX  = 45;    % [rad/s]
KP_MIN = 0;     % [Nm/rad]
KP_MAX = 500;   % [Nm/rad]
KD_MIN = 0;     % [Nm*s/rad
KD_MAX = 5;     % [Nm*s/rad
T_MIN  =-18;    % [Nm]
T_MAX  = 18;    % [Nm]

position = floor((max(min(position,P_MAX) ,P_MIN)  - P_MIN )*65535/(P_MAX  - P_MIN));
velocity = floor((max(min(velocity,V_MAX) ,V_MIN)  - V_MIN )*4095 /(V_MAX  - V_MIN));
K_p      = floor((max(min(K_p     ,KP_MAX),KP_MIN) - KP_MIN)*4095 /(KP_MAX - KP_MIN));
K_d      = floor((max(min(K_d     ,V_MAX) ,V_MIN)  - KD_MIN)*4095 /(KD_MAX - KD_MIN));
T_ff     = floor((max(min(T_ff    ,V_MAX) ,V_MIN)  - T_MIN )*4095 /(T_MAX  - T_MIN));

p  = dec2bin(position);
p  = [repmat('0', 1, 16-length(p)),p];
v  = dec2bin(velocity);
v  = [repmat('0', 1, 12-length(v)),v];
kp = dec2bin(K_p);
kp  = [repmat('0', 1, 12-length(kp)),kp];
kd = dec2bin(K_d);
kd  = [repmat('0', 1, 12-length(kd)),kd];
t  = dec2bin(T_ff);
t  = [repmat('0', 1, 12-length(t)),t];

B = repmat('0', 8, 8);

B(1,:) = p(1:8);
B(2,:) = p(9:16);
B(3,:) = v(1:8);
B(4,:) = [v(9:12),kp(1:4)];
B(5,:) = kp(5:12);
B(6,:) = kd(1:8);
B(7,:) = [kd(9:12),t(1:4)];
B(8,:) = t(5:12);

B  = bin2dec(B);

b = uint8(B);

== matlab function CAN_2_Legs/MATLAB Function1 ==
function danger = isDanger(Pmux)
    % Pmux position matrix radians
    %       [p(ID1),p(ID2),p(ID3),p(IDN)]
    
    p1Max = .5; 
    p1Min = -.5;
    p2Max = .5;
    p2Min = -.5;
    
    P1 = Pmux(1:2:end);
    P2 = Pmux(2:2:end);
    
    
    danger = 0;
    if((0<sum(P1>p1Max + P1<p1Min)) || (0<sum(P2>p2Max + P2<p2Min)))
        danger = 1;
    end

== matlab function CAN_2_Legs/Subsystem2/MATLAB Function2 ==
function p = ramp(to,t,po,pf,pc, tstep)
    slope = (pf - po)/tstep;
    p = po + slope*(t-to);
    if((p > pf&& slope>0) || (p < pf && slope<0))
        p = pf;
    end
    if(t==0)
        p = pc;
    end

== matlab function CAN_2_Legs/Subsystem/MATLAB Function2 ==
function p = ramp(to,t,po,pf,pc, tstep)
    slope = (pf - po)/tstep;
    p = po + slope*(t-to);
    if((p > pf&& slope>0) || (p < pf && slope<0))
        p = pf;
    end
    if(t==0)
        p = pc;
    end
